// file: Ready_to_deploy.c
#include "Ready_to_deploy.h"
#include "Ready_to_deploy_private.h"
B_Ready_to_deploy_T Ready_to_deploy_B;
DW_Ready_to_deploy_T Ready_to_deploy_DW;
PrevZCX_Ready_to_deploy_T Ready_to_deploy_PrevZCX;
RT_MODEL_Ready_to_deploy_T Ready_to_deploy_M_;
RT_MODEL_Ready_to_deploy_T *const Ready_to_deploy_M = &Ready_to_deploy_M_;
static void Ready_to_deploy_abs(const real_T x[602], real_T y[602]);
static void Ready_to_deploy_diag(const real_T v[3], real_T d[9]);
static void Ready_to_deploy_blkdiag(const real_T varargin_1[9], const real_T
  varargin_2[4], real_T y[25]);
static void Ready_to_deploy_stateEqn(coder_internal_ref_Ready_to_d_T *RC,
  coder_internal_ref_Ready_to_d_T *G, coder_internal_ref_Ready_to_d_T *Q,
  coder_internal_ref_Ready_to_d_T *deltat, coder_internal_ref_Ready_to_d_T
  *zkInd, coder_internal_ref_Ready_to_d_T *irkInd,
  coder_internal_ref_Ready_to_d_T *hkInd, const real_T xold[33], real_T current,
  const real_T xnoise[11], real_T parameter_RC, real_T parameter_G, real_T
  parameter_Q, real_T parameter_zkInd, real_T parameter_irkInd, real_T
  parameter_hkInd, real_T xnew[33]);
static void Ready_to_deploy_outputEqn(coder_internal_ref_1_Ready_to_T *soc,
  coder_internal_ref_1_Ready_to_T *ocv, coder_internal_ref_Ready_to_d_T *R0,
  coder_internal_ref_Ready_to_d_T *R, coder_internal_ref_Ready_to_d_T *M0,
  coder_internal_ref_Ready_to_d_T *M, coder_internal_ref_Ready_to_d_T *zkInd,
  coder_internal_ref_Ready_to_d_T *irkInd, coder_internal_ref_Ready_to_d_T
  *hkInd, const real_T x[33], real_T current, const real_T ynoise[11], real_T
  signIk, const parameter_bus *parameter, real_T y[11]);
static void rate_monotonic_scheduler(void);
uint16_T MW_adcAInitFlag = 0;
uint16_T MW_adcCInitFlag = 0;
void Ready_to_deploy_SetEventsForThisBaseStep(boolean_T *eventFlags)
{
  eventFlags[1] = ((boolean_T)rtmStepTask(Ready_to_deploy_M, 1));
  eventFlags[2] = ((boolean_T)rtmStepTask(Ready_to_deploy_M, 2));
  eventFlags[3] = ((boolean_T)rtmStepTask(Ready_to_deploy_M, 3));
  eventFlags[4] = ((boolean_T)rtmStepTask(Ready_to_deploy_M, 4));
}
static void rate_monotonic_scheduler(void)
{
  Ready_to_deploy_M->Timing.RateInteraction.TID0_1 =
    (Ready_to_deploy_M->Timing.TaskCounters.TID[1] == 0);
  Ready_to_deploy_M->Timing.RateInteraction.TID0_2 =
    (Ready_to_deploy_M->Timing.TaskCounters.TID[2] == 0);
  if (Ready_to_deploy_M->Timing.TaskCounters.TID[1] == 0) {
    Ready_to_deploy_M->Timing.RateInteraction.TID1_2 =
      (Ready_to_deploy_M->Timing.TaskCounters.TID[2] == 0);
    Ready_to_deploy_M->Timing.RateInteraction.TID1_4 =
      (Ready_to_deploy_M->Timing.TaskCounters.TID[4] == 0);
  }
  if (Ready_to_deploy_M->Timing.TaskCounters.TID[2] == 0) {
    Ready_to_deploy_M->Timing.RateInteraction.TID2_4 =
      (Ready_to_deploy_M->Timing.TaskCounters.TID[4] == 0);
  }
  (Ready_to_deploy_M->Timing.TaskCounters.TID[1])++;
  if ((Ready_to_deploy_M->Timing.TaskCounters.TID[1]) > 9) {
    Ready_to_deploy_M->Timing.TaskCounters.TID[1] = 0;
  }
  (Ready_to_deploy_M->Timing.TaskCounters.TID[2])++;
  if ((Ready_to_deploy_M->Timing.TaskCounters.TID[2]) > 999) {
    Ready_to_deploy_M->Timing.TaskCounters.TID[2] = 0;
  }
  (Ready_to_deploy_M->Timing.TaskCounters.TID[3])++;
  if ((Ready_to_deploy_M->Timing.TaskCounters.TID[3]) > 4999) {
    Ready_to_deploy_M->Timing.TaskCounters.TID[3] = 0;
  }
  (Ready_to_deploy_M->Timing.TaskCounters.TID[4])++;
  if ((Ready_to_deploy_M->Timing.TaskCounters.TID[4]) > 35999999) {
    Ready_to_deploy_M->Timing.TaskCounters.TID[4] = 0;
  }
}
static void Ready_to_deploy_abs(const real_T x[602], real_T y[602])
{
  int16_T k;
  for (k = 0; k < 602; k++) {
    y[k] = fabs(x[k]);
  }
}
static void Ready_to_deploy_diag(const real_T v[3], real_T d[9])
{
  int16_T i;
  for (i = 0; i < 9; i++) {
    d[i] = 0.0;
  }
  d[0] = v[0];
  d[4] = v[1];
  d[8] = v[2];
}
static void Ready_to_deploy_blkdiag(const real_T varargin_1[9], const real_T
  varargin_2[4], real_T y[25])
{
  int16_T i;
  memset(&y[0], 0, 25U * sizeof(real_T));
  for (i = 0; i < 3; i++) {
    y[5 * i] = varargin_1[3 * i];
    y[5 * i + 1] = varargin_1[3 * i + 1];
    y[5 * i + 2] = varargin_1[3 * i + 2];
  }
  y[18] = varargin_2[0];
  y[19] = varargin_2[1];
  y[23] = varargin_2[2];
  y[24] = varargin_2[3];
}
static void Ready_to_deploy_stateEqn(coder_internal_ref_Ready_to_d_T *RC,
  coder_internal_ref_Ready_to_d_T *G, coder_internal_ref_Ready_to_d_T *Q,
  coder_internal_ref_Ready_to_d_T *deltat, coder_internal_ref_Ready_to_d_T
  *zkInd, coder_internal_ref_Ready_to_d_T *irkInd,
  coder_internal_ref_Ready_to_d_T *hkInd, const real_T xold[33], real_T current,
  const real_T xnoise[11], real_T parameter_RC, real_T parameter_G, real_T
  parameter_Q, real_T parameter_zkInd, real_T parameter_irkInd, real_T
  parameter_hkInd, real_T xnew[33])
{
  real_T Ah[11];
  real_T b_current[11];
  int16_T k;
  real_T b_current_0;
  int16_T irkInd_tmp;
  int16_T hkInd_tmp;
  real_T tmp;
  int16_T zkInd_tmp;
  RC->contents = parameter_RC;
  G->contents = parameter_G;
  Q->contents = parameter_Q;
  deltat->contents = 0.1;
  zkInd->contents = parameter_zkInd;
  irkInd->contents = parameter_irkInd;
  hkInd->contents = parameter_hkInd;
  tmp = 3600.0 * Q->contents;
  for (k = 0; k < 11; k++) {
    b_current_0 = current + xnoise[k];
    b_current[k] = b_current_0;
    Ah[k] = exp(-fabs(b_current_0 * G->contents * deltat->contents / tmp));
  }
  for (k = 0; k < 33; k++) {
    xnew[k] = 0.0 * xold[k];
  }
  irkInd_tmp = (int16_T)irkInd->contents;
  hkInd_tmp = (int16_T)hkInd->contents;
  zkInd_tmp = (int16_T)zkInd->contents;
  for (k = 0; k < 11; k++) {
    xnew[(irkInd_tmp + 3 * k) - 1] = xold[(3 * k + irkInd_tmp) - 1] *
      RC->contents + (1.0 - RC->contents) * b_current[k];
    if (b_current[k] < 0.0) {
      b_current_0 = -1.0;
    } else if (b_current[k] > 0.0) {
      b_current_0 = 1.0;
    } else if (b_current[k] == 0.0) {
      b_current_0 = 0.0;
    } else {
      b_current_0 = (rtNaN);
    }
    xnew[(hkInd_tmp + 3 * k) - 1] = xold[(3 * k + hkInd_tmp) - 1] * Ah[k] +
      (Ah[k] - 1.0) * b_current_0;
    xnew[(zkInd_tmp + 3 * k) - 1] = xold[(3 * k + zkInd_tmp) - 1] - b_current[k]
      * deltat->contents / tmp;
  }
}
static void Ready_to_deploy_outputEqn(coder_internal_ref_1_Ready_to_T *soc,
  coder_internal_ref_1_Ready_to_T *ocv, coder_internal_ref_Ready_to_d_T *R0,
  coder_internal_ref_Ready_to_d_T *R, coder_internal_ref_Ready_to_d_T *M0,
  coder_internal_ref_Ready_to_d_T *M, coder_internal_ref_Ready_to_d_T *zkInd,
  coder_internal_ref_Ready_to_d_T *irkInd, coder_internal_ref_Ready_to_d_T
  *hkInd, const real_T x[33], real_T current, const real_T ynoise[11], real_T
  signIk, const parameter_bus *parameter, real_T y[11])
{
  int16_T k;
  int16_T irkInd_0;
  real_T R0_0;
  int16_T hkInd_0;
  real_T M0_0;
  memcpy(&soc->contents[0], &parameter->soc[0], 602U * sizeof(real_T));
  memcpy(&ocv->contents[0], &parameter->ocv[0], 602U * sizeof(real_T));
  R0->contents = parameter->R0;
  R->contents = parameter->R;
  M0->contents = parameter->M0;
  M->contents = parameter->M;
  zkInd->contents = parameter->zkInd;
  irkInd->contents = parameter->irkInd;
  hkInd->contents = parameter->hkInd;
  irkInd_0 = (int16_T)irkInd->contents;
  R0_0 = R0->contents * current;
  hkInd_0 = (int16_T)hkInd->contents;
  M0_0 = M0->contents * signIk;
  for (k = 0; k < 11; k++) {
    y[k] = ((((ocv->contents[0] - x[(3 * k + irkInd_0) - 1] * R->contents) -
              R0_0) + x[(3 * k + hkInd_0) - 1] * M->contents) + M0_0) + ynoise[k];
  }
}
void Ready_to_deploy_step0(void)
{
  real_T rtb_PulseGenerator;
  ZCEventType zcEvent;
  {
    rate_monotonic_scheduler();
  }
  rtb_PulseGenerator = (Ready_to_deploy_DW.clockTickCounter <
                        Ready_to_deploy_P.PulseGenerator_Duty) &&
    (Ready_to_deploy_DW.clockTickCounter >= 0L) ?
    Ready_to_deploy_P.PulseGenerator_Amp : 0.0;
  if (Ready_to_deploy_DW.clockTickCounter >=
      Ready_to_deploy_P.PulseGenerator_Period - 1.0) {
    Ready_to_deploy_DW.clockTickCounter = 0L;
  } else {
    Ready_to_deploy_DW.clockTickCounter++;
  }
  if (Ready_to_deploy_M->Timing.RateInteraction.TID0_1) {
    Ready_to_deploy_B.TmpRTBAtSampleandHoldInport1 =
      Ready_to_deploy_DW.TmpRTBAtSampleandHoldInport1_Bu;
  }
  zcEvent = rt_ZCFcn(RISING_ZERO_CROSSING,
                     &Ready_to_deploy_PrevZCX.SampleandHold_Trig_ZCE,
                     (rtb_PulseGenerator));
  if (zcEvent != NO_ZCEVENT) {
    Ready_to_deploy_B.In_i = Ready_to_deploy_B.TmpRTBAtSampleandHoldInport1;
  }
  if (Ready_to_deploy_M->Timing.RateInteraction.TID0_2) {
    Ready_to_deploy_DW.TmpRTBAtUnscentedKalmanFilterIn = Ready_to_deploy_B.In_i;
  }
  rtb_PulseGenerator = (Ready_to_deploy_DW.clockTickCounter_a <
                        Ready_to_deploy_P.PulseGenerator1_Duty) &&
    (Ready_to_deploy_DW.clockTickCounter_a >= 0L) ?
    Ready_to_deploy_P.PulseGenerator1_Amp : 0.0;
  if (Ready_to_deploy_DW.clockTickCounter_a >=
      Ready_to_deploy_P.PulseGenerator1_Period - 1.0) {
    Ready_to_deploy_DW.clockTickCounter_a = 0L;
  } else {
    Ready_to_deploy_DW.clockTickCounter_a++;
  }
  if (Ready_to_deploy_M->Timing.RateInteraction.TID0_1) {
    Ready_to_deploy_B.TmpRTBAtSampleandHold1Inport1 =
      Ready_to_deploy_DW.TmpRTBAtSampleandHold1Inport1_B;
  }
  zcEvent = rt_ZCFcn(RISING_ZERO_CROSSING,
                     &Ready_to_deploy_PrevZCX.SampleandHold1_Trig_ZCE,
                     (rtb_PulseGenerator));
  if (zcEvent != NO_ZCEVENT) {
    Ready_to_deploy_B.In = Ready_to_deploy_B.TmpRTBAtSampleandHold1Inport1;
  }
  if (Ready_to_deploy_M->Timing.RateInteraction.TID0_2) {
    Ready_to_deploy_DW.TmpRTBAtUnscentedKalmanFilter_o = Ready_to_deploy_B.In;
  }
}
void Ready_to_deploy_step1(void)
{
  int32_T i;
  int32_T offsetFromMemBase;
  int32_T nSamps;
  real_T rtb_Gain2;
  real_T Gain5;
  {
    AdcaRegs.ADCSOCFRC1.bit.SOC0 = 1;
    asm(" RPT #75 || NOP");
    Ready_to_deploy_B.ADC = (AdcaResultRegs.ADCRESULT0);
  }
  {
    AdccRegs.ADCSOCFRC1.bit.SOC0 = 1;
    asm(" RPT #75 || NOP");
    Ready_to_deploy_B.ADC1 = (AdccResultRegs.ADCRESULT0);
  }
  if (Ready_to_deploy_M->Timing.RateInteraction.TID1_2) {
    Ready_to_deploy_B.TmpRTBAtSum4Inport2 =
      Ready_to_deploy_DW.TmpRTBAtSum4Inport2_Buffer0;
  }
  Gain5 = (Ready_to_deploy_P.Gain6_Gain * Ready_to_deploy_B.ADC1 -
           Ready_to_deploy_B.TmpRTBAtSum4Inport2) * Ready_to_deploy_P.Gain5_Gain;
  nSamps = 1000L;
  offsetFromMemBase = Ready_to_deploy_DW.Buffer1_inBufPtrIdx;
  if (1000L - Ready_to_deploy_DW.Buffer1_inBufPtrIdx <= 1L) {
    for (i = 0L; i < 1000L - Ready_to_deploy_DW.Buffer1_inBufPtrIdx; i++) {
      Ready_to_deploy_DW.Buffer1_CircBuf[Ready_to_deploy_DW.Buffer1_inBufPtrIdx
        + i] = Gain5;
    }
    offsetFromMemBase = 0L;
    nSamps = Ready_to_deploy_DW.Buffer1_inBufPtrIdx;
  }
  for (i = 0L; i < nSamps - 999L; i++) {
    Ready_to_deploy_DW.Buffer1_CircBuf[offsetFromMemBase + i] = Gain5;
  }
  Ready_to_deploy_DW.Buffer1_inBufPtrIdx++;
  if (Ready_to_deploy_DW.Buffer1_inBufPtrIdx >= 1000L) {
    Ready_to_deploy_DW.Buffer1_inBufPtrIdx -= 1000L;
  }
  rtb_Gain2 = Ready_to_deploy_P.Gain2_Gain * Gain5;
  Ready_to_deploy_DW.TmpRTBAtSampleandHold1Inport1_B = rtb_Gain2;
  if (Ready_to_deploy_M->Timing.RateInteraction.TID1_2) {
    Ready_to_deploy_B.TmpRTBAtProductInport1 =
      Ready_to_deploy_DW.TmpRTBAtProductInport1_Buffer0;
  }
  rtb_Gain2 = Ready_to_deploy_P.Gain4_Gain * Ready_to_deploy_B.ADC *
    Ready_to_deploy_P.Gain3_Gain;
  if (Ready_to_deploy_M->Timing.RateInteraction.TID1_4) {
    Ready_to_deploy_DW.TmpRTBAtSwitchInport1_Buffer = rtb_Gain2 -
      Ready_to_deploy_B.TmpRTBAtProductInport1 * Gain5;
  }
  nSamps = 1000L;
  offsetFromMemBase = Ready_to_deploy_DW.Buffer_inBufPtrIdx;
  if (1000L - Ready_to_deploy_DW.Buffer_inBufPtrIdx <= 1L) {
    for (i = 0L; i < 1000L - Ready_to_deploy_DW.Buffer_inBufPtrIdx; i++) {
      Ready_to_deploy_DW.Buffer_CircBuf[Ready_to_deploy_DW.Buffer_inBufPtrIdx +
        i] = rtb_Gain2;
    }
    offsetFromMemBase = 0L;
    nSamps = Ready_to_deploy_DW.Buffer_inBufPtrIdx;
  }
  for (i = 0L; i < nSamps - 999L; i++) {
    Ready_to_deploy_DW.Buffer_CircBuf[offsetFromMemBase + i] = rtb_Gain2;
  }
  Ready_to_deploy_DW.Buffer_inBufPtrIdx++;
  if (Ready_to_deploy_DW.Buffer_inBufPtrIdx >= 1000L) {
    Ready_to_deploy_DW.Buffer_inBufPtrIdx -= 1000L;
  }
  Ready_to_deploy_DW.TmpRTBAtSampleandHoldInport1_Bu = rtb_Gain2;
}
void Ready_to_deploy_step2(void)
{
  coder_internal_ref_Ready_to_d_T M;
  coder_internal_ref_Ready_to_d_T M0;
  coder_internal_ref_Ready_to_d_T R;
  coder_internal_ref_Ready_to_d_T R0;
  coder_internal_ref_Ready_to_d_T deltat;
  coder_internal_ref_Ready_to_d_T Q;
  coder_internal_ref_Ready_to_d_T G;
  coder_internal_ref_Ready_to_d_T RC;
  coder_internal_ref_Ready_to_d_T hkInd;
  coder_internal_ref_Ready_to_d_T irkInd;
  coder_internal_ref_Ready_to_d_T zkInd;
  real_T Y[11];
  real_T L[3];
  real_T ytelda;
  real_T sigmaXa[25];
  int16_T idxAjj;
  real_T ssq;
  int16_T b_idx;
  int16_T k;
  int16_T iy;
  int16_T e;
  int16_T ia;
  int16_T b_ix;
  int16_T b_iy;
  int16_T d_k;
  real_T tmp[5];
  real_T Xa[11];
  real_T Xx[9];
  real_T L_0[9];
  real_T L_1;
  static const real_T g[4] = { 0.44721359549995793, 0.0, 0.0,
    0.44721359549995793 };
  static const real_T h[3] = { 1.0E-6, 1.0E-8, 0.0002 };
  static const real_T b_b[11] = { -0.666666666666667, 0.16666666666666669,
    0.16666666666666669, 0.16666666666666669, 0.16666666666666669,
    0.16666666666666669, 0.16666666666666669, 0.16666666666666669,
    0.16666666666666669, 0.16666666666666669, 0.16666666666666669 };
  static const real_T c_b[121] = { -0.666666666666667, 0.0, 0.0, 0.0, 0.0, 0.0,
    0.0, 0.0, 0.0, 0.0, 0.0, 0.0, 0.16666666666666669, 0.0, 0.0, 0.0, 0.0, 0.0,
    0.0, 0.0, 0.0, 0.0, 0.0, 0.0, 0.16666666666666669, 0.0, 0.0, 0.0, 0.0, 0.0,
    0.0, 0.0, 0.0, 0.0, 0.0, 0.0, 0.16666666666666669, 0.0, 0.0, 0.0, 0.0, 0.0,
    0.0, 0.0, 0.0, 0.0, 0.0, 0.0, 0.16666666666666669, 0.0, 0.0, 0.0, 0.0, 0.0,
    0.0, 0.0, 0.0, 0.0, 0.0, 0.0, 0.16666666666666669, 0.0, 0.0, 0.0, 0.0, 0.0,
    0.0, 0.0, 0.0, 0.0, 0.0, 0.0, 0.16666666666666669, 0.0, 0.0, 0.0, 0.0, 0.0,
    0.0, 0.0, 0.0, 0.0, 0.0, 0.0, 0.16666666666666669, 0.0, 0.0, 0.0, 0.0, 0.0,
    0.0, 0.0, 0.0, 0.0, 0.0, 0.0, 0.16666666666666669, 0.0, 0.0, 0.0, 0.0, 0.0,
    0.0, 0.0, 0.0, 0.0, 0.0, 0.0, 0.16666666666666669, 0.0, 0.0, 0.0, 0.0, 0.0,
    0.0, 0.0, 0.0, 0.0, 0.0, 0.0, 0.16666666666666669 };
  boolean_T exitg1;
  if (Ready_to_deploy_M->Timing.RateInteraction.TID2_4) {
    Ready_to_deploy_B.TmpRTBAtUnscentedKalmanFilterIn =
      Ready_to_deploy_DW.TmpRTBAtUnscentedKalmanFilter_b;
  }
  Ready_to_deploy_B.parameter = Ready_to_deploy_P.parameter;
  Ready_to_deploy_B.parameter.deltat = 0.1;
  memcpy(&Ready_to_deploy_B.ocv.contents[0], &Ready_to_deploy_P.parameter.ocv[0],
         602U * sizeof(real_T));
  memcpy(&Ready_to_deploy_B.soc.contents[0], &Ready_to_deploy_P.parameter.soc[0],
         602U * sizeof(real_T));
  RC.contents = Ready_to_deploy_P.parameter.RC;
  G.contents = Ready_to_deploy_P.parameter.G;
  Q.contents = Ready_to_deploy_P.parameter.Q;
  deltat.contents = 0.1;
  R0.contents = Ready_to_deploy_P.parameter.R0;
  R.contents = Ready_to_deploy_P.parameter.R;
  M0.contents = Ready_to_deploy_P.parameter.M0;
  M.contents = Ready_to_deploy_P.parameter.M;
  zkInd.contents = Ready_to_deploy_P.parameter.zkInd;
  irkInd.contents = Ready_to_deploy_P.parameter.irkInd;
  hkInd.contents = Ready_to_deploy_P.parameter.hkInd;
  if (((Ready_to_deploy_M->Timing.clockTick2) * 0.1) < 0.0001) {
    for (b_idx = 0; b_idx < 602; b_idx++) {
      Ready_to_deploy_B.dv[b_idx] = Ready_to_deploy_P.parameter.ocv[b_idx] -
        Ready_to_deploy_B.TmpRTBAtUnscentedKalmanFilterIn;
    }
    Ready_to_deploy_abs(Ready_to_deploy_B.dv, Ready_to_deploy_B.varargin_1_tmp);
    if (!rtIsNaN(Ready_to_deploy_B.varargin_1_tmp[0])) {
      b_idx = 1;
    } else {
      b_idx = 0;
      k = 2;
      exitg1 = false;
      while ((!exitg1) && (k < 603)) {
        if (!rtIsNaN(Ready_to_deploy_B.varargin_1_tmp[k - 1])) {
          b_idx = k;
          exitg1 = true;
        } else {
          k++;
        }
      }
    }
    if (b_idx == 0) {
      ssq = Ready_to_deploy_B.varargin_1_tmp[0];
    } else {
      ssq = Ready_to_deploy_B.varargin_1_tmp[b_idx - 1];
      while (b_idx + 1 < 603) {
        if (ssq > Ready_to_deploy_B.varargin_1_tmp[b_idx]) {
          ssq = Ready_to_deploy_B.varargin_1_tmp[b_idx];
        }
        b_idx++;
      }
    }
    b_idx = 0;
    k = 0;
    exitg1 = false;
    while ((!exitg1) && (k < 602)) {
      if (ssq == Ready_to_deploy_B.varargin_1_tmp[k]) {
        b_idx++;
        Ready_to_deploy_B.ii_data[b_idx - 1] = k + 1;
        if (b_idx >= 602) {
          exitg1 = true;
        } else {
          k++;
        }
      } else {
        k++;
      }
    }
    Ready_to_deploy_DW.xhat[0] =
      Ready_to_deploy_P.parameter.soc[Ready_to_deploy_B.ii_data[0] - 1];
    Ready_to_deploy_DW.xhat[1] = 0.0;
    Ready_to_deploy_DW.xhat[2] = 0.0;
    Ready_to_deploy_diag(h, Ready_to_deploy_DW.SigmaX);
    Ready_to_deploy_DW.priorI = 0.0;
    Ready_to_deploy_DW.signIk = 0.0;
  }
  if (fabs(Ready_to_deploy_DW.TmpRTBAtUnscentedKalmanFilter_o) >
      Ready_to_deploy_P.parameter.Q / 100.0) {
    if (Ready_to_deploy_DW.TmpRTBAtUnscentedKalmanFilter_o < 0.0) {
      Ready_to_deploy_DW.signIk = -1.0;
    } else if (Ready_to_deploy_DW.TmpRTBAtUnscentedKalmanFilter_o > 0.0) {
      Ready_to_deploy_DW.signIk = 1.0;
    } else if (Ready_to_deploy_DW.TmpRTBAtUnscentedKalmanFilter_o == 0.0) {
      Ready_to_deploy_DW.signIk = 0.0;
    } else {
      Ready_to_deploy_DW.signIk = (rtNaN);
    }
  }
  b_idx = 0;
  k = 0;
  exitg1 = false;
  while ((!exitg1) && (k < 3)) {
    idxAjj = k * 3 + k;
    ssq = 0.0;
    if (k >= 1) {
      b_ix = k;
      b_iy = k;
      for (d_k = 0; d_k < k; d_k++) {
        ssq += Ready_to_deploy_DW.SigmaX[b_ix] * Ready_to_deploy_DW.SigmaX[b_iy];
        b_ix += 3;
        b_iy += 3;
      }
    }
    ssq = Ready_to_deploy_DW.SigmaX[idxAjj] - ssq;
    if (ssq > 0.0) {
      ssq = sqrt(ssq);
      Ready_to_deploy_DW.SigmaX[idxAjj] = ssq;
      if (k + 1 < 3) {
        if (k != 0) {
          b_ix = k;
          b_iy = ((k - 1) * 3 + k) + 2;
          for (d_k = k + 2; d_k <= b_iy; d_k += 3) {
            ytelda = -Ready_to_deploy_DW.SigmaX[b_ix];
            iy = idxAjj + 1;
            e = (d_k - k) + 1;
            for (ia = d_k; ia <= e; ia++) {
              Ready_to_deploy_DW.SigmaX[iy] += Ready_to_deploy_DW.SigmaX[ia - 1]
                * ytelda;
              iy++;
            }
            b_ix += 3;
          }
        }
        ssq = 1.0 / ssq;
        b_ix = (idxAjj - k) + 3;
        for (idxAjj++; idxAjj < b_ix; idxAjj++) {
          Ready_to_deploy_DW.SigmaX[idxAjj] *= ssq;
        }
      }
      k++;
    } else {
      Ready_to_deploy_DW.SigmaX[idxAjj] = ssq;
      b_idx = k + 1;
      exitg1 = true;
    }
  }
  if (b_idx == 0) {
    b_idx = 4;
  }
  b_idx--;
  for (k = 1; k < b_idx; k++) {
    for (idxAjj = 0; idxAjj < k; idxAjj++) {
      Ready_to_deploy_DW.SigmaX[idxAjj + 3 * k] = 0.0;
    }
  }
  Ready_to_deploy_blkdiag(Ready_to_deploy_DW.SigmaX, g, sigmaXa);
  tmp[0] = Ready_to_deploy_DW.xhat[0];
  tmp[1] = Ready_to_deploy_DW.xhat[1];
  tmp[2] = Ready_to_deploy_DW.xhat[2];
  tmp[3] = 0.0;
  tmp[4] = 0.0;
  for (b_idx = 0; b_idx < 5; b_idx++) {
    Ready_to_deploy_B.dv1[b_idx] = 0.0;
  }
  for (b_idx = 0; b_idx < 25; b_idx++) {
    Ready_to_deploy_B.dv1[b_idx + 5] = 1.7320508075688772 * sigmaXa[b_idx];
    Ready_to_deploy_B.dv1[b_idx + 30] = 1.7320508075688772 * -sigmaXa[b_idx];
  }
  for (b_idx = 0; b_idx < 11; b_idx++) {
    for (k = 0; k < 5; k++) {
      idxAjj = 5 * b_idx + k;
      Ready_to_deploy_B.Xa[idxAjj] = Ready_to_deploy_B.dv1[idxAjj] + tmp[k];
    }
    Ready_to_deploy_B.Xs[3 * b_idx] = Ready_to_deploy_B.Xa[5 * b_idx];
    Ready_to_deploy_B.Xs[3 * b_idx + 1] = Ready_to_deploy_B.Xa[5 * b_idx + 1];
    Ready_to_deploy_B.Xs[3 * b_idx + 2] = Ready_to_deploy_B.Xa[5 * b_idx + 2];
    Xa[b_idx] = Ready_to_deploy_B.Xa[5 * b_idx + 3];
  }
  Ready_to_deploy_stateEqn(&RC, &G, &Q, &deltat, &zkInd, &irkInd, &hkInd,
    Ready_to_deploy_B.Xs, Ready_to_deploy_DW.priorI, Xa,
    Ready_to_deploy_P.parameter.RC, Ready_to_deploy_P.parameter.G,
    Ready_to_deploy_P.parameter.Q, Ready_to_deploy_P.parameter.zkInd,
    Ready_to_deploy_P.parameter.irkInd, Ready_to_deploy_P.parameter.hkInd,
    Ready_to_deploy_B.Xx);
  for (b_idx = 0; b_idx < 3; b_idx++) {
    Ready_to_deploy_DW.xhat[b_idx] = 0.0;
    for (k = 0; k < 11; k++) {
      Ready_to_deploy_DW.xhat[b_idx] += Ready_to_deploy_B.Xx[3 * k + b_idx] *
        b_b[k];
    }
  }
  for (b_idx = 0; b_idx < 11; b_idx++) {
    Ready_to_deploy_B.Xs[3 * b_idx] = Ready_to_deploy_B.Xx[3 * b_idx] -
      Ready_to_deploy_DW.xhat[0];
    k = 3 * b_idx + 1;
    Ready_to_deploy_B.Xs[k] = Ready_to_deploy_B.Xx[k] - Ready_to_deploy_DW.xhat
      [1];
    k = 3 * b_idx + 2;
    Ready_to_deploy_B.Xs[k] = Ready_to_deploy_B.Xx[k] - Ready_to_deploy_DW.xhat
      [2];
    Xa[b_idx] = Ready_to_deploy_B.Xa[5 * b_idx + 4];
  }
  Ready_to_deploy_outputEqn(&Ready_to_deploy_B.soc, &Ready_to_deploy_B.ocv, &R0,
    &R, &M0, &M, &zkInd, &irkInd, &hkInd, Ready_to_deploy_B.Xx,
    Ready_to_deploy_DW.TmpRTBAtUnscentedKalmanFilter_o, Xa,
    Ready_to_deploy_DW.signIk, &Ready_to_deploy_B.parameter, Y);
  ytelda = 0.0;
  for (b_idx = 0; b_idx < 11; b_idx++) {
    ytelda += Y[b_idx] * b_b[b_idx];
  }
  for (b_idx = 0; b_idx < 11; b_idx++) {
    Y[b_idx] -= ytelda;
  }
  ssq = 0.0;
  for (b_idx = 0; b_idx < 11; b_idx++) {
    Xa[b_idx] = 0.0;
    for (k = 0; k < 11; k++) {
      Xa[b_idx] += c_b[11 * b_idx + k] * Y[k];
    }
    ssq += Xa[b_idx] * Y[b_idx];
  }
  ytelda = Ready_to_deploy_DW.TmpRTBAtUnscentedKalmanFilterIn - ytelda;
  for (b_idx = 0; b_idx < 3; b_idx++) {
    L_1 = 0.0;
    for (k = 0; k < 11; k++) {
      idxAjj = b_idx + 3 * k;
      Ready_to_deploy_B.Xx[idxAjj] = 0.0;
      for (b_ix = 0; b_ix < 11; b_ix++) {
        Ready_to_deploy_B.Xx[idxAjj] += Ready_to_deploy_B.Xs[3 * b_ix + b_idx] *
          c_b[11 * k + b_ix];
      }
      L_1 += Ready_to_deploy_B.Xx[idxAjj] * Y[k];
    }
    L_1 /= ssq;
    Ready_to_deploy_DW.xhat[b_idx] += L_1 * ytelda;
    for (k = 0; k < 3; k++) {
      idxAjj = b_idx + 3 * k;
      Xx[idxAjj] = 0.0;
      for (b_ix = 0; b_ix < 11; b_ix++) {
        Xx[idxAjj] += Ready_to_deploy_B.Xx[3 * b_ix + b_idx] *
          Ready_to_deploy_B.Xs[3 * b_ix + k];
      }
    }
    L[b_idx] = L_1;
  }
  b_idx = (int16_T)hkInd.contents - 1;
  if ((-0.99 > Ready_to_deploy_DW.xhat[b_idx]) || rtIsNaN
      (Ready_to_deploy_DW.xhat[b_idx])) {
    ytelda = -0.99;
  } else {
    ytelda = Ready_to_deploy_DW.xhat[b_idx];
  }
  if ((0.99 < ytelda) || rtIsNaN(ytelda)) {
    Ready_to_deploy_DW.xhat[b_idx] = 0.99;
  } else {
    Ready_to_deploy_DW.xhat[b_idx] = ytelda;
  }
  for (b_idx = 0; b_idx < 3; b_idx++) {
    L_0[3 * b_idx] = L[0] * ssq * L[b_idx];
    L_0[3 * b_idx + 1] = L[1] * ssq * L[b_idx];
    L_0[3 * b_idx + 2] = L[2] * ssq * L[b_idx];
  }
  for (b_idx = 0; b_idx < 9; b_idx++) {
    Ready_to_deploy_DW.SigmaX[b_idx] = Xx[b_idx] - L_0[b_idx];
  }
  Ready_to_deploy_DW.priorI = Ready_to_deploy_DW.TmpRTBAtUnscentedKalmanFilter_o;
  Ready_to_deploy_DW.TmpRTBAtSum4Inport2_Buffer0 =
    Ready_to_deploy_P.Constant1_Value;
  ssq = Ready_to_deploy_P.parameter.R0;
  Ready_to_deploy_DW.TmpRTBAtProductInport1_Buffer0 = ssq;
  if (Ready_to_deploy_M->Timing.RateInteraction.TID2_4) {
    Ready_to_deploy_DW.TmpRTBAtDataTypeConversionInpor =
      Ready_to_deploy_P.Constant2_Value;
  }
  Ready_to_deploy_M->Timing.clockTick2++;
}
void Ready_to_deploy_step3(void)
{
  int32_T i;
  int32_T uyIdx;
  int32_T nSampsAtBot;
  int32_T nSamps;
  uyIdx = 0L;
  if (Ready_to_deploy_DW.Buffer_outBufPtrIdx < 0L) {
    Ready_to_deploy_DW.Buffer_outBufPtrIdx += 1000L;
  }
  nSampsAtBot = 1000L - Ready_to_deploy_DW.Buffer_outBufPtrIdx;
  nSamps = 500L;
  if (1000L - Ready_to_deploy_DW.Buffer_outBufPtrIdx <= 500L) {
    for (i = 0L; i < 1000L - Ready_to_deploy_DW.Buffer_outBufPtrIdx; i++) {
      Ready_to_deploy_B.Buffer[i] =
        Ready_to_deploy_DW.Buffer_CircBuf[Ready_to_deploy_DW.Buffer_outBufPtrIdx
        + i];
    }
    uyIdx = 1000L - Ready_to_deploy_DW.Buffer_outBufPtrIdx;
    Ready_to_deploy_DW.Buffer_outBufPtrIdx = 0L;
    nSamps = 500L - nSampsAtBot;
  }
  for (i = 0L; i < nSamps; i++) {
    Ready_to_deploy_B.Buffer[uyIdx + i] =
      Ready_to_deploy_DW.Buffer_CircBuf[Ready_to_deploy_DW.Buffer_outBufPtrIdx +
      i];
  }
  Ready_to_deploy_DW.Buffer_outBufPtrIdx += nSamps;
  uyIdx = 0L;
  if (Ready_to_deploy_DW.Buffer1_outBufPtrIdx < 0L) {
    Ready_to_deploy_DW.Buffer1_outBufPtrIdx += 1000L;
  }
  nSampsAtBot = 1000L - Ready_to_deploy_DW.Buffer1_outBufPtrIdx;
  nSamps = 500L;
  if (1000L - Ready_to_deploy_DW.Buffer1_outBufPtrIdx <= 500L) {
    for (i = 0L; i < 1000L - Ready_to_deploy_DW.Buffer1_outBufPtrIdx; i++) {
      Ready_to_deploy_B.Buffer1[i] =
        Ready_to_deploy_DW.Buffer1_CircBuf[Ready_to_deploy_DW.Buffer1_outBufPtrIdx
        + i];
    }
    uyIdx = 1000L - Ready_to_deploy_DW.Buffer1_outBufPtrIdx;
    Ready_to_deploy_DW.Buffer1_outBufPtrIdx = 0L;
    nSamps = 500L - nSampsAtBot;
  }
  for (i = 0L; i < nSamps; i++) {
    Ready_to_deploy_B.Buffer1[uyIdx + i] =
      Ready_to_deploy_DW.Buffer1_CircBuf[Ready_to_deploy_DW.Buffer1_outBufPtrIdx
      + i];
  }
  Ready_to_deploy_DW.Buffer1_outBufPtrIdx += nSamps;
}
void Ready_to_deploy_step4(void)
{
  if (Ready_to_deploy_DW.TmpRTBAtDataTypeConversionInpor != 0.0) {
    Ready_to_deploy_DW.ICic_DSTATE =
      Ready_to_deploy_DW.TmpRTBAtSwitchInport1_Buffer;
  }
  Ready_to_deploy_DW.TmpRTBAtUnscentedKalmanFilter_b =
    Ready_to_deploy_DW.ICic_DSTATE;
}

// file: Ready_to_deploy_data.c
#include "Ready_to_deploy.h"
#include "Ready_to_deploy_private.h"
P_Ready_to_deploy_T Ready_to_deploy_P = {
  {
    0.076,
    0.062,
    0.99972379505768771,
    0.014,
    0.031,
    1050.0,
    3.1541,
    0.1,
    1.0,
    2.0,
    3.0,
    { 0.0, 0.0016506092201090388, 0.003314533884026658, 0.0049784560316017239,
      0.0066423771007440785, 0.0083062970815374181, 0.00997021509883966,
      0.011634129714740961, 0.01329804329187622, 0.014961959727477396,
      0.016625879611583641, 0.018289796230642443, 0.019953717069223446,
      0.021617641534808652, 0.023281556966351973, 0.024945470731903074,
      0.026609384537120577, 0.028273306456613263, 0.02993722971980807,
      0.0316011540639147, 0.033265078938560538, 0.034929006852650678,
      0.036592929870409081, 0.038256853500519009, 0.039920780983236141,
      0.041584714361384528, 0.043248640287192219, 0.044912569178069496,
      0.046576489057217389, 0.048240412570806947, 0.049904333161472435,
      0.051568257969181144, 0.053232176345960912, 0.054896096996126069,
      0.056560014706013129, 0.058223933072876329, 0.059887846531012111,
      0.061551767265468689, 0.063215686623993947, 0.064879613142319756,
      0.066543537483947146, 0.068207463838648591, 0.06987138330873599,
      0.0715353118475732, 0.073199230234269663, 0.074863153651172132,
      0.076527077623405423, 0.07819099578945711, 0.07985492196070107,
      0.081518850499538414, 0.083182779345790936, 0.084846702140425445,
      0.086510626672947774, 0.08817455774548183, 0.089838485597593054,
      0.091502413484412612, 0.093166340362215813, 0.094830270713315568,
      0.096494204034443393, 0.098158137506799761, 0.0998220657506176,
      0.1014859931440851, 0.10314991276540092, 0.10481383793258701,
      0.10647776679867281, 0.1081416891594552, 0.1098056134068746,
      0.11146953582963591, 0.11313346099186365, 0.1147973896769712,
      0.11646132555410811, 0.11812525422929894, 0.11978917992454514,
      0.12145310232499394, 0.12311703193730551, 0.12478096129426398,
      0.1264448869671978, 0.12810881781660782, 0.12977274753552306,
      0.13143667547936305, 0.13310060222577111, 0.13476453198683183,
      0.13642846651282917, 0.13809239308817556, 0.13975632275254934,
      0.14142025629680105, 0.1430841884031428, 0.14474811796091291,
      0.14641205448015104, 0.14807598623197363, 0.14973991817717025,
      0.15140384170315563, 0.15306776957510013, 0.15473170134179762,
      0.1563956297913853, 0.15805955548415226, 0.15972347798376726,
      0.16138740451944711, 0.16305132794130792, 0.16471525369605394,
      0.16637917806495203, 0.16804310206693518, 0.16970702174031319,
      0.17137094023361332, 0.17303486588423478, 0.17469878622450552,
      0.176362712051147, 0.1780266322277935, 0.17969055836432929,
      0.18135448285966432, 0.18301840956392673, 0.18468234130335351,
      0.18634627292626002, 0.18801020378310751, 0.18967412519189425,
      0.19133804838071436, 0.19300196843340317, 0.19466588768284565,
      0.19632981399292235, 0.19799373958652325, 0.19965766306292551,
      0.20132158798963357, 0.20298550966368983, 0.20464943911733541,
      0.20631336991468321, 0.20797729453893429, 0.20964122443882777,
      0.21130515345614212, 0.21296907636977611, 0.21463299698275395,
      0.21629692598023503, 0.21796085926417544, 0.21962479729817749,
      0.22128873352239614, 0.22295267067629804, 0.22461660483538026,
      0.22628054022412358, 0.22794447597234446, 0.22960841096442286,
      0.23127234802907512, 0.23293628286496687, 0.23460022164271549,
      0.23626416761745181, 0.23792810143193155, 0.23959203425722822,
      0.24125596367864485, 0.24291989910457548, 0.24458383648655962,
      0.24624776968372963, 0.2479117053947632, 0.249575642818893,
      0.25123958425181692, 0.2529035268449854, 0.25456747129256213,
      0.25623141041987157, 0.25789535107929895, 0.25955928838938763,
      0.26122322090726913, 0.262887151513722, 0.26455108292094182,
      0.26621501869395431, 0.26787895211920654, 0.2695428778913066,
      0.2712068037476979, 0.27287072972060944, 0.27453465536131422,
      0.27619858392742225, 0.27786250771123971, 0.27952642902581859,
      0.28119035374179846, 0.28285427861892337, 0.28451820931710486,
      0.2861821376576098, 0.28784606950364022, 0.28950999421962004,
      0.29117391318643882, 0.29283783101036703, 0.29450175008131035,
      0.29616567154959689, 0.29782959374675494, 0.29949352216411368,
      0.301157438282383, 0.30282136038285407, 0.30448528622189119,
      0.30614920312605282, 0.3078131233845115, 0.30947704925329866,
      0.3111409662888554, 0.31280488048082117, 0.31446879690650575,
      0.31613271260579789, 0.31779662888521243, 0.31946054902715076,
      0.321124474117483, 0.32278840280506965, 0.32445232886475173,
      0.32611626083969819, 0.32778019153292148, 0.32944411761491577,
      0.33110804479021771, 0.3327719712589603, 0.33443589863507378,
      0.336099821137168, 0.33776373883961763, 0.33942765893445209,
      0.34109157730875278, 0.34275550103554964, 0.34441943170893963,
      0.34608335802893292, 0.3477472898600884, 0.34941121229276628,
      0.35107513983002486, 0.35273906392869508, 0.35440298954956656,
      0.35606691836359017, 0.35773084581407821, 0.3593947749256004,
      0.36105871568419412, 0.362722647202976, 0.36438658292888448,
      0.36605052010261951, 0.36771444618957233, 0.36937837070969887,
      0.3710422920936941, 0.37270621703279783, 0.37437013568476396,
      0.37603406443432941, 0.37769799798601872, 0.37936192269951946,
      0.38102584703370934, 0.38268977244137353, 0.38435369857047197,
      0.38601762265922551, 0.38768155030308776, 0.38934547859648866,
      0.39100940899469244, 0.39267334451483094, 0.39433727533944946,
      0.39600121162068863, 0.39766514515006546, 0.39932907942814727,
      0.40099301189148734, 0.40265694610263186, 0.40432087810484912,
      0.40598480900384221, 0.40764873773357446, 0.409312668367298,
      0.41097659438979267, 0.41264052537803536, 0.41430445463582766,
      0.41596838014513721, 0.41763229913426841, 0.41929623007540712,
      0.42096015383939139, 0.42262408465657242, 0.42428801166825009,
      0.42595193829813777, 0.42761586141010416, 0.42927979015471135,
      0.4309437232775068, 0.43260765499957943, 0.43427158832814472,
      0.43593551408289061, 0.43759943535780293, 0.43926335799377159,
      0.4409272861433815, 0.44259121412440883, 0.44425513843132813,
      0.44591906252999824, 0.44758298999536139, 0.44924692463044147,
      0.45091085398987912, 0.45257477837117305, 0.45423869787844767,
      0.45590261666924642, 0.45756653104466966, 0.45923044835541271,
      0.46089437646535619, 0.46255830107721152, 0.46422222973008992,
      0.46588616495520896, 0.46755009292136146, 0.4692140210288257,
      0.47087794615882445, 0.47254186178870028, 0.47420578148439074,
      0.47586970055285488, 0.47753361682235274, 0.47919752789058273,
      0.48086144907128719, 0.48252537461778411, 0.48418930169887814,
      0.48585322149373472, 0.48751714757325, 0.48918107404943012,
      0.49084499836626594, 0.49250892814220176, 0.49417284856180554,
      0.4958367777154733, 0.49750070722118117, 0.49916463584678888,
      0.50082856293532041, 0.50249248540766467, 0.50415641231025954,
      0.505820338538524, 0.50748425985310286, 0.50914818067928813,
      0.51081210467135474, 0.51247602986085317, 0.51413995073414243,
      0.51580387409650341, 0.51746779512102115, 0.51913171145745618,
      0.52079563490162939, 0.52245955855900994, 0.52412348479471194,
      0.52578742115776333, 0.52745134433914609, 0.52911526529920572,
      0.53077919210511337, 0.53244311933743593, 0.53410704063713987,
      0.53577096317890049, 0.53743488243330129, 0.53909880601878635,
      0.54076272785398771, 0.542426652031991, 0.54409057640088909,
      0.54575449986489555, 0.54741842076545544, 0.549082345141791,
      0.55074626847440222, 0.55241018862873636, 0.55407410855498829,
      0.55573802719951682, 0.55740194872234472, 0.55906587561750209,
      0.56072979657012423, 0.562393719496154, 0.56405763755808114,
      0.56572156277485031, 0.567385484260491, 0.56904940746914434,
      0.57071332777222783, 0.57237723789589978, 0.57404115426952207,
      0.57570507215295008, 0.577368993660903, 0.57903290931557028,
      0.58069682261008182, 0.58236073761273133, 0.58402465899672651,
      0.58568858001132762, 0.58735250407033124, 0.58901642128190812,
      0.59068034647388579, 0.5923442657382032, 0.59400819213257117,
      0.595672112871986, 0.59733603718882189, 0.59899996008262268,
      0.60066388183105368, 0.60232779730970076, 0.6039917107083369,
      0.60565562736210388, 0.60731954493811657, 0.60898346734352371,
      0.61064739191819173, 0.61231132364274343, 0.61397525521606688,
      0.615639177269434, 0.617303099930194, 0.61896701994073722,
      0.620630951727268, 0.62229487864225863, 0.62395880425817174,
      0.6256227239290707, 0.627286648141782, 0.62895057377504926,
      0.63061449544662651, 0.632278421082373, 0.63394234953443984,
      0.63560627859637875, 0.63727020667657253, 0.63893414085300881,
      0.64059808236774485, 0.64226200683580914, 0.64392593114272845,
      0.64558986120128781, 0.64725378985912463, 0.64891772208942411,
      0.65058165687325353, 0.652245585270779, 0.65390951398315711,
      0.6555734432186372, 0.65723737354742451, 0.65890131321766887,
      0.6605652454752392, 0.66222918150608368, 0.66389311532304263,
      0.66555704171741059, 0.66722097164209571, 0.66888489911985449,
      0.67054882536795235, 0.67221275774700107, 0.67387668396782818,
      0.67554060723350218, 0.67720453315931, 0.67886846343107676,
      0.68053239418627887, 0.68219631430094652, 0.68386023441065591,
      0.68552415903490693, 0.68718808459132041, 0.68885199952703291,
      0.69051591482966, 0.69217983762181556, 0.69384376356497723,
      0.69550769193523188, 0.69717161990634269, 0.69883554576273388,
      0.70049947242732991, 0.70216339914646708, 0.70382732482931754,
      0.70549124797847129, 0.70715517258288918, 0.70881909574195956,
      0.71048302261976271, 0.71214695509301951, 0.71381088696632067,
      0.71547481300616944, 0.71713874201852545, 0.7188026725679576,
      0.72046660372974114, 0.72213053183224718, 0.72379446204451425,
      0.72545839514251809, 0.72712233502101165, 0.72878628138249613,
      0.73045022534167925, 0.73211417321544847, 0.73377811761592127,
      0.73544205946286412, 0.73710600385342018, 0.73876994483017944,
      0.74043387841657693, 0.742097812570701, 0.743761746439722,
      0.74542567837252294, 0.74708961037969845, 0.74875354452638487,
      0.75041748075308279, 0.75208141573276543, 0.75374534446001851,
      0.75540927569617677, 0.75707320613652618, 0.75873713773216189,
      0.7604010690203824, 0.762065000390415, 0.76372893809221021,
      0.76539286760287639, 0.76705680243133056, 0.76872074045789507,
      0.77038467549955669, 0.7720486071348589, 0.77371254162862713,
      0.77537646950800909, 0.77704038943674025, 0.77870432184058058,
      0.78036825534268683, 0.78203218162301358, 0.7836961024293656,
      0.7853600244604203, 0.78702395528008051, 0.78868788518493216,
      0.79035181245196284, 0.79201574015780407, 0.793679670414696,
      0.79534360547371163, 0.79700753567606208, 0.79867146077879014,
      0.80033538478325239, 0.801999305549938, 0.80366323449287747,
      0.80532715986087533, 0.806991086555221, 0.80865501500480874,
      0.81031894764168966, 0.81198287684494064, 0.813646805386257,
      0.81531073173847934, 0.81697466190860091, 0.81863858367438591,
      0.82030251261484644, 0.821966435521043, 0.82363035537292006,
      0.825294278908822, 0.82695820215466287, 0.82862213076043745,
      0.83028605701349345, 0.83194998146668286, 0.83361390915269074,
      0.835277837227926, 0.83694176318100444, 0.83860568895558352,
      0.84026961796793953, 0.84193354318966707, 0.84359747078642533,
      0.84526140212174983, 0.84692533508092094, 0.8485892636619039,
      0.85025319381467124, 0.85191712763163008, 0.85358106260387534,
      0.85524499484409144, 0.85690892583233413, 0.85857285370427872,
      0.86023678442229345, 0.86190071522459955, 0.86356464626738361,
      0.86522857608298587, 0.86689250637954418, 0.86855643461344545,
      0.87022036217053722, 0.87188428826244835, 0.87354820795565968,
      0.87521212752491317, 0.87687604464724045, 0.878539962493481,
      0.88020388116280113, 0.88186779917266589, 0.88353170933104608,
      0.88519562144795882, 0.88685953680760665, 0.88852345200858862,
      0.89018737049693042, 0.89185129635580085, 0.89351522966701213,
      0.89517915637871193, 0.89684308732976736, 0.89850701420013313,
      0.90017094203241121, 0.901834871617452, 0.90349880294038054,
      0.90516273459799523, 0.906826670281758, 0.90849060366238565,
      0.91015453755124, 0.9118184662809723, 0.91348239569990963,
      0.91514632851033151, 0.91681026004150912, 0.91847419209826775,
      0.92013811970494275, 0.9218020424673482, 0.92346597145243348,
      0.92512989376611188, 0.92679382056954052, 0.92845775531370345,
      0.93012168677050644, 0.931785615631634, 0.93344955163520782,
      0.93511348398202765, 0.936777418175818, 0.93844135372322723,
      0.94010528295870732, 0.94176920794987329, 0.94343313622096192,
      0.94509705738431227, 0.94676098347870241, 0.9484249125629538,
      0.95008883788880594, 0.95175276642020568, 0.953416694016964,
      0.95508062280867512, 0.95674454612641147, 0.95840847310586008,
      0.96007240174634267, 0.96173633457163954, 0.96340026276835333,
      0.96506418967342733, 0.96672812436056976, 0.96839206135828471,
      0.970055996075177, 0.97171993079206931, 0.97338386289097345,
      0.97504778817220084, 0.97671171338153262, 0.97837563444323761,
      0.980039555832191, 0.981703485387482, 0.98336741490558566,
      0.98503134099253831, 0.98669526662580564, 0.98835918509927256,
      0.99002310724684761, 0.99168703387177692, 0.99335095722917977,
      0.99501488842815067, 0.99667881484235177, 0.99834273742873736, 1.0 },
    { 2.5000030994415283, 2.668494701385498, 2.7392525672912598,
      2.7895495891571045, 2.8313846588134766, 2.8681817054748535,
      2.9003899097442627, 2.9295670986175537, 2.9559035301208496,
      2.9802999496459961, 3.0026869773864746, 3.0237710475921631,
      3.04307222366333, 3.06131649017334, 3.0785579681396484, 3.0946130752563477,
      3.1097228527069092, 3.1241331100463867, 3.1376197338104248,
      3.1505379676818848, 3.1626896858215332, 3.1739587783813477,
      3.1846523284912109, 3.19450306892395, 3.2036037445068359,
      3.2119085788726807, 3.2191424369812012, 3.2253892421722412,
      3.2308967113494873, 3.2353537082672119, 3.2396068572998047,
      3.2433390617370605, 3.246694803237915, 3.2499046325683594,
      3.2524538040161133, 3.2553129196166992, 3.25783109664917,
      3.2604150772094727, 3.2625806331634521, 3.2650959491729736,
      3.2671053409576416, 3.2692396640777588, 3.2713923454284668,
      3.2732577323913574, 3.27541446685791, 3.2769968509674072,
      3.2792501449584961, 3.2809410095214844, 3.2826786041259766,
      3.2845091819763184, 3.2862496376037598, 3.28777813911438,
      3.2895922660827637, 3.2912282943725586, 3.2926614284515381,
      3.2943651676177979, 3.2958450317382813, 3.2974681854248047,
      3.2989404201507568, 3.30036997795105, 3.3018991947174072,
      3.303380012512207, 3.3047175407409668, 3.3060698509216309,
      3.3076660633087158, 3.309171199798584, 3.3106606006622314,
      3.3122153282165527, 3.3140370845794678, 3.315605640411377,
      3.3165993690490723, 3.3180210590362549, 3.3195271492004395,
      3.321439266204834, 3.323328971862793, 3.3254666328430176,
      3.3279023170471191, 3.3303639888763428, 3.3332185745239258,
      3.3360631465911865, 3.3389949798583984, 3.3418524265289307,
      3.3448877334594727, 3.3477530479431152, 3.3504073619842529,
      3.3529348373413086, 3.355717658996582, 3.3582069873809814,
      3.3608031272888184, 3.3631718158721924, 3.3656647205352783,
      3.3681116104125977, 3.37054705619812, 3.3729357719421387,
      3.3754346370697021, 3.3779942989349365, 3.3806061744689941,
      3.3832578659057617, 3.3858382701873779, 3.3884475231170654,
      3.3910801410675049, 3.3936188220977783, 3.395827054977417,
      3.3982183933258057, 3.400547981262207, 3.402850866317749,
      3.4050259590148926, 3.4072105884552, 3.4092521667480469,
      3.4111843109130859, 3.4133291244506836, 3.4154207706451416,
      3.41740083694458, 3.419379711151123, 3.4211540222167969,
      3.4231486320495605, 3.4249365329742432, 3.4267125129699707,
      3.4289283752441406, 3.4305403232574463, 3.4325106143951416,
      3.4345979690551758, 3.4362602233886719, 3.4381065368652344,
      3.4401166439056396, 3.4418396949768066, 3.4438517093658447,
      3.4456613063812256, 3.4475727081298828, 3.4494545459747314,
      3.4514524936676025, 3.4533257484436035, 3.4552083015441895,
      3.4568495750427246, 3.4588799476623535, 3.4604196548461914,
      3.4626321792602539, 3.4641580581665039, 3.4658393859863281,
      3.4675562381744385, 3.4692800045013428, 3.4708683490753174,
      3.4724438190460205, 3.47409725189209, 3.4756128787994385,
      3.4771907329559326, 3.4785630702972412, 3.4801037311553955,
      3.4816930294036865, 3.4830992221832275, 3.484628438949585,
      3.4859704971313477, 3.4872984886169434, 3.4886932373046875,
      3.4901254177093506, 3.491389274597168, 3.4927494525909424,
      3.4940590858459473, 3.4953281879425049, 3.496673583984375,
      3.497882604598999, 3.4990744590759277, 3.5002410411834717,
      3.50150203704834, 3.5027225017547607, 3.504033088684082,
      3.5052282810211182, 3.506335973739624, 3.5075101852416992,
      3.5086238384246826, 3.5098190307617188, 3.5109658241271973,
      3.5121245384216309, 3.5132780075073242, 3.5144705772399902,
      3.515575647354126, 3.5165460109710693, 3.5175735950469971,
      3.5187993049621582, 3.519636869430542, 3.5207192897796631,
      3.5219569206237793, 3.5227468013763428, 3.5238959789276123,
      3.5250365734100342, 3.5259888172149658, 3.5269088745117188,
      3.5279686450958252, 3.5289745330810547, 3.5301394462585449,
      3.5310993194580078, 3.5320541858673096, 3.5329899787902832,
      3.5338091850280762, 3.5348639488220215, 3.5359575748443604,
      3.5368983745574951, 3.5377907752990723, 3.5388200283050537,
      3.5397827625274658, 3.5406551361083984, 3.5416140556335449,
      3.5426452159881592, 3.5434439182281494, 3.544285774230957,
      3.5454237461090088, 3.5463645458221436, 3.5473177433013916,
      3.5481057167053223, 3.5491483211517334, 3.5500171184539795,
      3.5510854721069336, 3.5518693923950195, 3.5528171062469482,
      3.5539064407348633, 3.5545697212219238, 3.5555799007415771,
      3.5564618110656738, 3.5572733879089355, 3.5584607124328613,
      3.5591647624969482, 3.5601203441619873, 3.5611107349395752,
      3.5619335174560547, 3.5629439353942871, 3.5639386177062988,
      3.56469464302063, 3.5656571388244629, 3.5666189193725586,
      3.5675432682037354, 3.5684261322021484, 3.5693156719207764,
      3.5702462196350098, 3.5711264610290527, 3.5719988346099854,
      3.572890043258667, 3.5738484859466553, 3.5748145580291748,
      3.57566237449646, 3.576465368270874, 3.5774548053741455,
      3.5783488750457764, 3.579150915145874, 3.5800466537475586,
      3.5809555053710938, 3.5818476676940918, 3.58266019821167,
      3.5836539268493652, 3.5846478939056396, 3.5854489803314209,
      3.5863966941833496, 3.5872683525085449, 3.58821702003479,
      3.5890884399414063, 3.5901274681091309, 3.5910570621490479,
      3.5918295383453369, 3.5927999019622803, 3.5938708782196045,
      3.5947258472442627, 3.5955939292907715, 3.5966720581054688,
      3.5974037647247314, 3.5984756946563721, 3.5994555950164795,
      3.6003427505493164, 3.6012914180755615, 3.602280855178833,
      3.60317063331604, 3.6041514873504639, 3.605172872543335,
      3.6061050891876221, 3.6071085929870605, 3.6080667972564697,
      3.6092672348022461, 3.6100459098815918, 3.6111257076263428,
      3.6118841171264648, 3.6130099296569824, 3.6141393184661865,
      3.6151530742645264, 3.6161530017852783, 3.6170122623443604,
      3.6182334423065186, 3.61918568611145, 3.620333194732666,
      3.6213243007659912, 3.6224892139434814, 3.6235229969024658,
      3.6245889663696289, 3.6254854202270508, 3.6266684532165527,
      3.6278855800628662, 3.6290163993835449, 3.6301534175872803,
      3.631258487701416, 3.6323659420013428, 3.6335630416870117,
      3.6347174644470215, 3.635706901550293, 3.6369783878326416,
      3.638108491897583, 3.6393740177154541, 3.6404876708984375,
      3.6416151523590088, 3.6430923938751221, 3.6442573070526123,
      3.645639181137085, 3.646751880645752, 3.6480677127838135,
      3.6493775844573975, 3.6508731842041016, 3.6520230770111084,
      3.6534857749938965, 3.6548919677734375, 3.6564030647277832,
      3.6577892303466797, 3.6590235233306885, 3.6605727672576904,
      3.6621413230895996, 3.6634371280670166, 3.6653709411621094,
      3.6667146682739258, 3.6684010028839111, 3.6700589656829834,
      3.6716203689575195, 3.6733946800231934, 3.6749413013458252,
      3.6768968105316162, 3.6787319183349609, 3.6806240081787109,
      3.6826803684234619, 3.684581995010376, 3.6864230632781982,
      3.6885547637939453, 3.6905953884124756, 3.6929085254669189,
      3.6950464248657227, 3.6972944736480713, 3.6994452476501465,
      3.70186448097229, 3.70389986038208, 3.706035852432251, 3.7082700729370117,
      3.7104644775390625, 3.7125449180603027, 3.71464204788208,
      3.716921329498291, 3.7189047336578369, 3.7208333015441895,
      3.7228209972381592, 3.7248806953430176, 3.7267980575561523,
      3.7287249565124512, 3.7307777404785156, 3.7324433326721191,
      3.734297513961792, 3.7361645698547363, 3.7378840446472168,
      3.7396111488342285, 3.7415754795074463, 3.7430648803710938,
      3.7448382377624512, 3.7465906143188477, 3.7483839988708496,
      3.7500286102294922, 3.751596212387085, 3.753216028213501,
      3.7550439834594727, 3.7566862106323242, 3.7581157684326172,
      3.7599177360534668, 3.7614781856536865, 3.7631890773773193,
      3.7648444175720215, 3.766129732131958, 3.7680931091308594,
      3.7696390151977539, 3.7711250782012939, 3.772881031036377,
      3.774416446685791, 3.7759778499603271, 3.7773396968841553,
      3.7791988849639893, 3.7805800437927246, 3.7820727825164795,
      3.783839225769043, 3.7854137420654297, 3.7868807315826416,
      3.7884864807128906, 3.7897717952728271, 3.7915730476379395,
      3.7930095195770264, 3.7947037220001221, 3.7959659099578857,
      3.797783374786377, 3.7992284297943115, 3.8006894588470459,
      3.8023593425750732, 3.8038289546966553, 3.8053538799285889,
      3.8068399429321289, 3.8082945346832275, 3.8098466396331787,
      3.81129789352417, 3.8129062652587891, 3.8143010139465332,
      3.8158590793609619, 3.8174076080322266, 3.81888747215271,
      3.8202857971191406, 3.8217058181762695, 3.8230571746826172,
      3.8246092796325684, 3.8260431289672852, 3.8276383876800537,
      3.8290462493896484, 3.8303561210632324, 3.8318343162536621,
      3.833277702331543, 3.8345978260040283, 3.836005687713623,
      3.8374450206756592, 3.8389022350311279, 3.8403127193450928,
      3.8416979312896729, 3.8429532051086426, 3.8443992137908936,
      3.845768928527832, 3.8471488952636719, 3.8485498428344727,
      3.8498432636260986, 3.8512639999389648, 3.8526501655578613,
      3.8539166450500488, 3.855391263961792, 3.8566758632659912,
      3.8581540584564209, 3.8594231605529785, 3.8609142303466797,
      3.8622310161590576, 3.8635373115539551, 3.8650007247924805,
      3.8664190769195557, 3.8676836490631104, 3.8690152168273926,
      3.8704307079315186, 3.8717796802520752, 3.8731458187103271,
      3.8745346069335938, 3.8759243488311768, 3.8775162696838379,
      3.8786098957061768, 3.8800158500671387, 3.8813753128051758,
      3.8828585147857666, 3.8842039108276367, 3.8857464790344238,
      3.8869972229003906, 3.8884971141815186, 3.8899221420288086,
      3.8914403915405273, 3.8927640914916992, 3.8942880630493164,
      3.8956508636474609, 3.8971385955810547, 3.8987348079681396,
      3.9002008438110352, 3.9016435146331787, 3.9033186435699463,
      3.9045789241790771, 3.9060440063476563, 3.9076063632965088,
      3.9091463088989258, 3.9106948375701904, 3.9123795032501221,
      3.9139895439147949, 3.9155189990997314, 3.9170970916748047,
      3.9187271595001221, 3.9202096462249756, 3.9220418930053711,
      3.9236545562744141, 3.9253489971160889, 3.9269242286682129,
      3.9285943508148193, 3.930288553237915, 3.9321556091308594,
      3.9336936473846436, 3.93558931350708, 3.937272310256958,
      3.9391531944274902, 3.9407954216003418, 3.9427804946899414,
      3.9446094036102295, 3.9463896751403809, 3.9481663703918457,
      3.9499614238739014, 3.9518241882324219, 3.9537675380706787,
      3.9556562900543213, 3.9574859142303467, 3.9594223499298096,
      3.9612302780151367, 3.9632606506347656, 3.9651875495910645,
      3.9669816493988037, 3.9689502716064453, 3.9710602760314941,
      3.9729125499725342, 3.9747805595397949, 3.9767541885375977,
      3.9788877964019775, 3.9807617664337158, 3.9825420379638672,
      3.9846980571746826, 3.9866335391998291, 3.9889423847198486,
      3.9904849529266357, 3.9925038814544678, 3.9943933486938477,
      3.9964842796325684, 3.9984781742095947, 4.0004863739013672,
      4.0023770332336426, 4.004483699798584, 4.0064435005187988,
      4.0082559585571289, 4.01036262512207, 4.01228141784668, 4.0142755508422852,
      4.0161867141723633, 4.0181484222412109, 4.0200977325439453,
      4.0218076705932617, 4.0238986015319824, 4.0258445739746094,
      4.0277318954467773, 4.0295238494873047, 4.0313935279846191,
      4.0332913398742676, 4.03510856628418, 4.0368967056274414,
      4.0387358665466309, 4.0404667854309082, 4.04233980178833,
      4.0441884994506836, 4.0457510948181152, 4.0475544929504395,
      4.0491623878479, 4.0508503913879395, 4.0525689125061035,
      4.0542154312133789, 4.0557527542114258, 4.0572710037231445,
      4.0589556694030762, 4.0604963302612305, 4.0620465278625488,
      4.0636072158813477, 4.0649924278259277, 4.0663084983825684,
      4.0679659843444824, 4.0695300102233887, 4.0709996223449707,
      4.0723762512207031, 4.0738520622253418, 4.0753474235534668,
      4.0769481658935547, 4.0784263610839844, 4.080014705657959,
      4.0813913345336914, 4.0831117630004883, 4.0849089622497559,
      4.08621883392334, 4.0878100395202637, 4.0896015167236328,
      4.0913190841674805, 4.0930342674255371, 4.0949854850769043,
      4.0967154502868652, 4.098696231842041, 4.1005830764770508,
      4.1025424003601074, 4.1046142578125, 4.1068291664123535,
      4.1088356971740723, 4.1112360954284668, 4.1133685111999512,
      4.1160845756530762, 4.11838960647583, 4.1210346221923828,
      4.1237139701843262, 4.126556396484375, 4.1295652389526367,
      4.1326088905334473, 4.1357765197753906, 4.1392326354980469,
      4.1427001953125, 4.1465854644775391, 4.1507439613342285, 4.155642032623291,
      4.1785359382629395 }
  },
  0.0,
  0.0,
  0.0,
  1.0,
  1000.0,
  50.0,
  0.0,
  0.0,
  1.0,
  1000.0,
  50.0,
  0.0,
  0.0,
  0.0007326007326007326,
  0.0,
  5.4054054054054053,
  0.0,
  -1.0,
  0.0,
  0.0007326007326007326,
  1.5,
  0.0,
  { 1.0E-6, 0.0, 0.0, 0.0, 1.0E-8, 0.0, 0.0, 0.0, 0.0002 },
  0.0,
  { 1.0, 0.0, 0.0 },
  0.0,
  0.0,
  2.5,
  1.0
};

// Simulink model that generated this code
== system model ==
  MemoryCopy#1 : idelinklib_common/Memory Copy  <- 1: Buffer1
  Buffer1 : Buffer  N=500  <- 1: Gain5
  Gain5 : Gain  Gain=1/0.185  <- 1: Sum#1
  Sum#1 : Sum  Inputs=+-  <- 1: Gain6, 2: Constant1
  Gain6 : Gain  Gain=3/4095  <- 1: ADC1
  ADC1 : c2802xlib/ADC
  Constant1 : Constant  Value=2.5
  MemoryCopy#2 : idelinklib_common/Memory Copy  <- 1: Buffer
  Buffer : Buffer  N=500  <- 1: Gain3
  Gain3 : Gain  Gain=1.5  <- 1: Gain4
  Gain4 : Gain  Gain=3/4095  <- 1: ADC
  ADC : c2802xlib/ADC
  MATLABFunction#1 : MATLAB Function  <- 1: SampleandHold, 2: SampleandHold1, 3: DigitalClock#1, 4: SampleandHold#1, 5: Constant#1, 6: UnitDelay#1, 7: UnitDelay#2, 8: UnitDelay#3, 9: UnitDelay#4
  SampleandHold : dspsigops/Sample and Hold  <- 1: Gain3, Trigger: PulseGenerator
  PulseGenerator : DiscretePulseGenerator  Period=1e-1  PulseWidth=5
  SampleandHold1 : dspsigops/Sample and Hold  <- 1: Gain2, Trigger: PulseGenerator1
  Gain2 : Gain  Gain=-1  <- 1: Gain5
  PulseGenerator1 : DiscretePulseGenerator  Period=1e-1  PulseWidth=5
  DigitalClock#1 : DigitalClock
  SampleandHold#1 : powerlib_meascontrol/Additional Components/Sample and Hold  <- 1: Sum#2, 2: Constant2
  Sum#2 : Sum  Inputs=-+  <- 1: Product#1, 2: Gain3
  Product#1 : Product  <- 1: R0, 2: Gain5
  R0 : Constant  Value=parameter.R0
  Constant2 : Constant
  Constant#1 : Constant  Value=parameter
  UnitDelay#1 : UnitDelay  InitialCondition=[1;0;0]  <- 1: MATLABFunction#1/3
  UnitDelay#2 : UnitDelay  InitialCondition=diag([1e-6 1e-8 2e-4])  <- 1: MATLABFunction#1/4
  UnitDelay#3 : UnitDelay  <- 1: MATLABFunction#1/5
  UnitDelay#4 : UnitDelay  <- 1: MATLABFunction#1/6
== matlab function MATLABFunction#1 ==
function [zk,zkbnd,xhat,SigmaX,priorI,signIk] = iterSPKF(vk,ik,t,v0,parameter,xhat,SigmaX,priorI,signIk)
parameter.deltat=1e-1;
SigmaX0 = diag([1e-6 1e-8 2e-4]);
SigmaV = 2e-1;
SigmaW = 2e-1;
Snoise = chol(blkdiag(SigmaW,SigmaV),'lower');
irk0 = 0;
hk0 = 0;
zkInd = 1;
irkInd = 2;
hkInd = 3;
ocv=parameter.ocv;
soc=parameter.soc;
Nx = 3;
Nw = 1;
Nv = 1;
Na = Nx+Nw+Nv;
h = sqrt(3);
alpha1 = (h*h-Na)/(h*h);
alpha2 = 1/(2*h*h);
alpham = [alpha1; alpha2*ones(2*Na,1)];
alphac = alpham;
RC      = parameter.RC;
G       = parameter.G;
Q       = parameter.Q;
deltat  = parameter.deltat;
R0      = parameter.R0;
R       = parameter.R;
M0      = parameter.M0;
M       = parameter.M;
zkInd   = parameter.zkInd;
irkInd  = parameter.irkInd;
hkInd   = parameter.hkInd;

eta     = 1;
if ik<0 
ik=ik*eta;
end

if t<1e-4
j1=find(min(abs(ocv-v0))==abs(ocv-v0));
j=j1(1,:);
SOC0 = soc(j);
xhat = [SOC0;irk0;hk0];
SigmaX = SigmaX0;
priorI = 0;
signIk = 0;
end

I       =  priorI;
if abs(ik)>Q/100
signIk = sign(ik);
end
xhata = [xhat; zeros([Nw+Nv 1])];
sigmaXa = chol(SigmaX,'lower');
sigmaXa= blkdiag(sigmaXa,Snoise);
Xa = xhata(:,ones([1 2*Na+1])) + h*[zeros([Na 1]),sigmaXa,-sigmaXa];
Xx = stateEqn(Xa(1:Nx,:),I,Xa(Nx+1:Nx+Nw,:),parameter);
xhat = Xx*alpham;
Xs = Xx - xhat(:,ones([1 2*Na+1]));
SigmaX = Xs*diag(alphac)*Xs';
I = ik;
yk = vk;
Y = outputEqn(Xx,I,Xa(5,:),signIk,parameter);
yhat = Y*alpham;
Ys = Y - yhat(:,ones([1 2*Na+1]));
SigmaXY = Xs*diag(alphac)*Ys';
SigmaY = Ys*diag(alphac)*Ys';
L = SigmaXY/SigmaY;
ytelda = yk - yhat;
xhat = xhat + L*ytelda;
xhat(hkInd) = min(0.99,max(-0.99,xhat(hkInd)));
SigmaX = SigmaX - L*SigmaY*L';
priorI = ik;
zk = xhat(zkInd);
zkbnd = 3*sqrt(SigmaX(zkInd,zkInd));
function xnew = stateEqn(xold,current,xnoise,parameter)
current = current + xnoise;
RC      = parameter.RC;
G       = parameter.G;
Q       = parameter.Q;
deltat  = parameter.deltat;
zkInd   = parameter.zkInd;
irkInd  = parameter.irkInd;
hkInd   = parameter.hkInd;
Ah = exp(-abs(current*G*deltat/(3600*Q)));
xnew = 0*xold;
xnew(irkInd,:) = RC*xold(irkInd,:) + (1-RC)*current;
xnew(hkInd,:) = Ah.*xold(hkInd,:) + (Ah-1).*sign(current);
xnew(zkInd,:) = xold(zkInd,:) - current*deltat/(3600*Q);
end
function y = outputEqn(x,current,ynoise,signIk,parameter)
soc     = parameter.soc;
ocv     = parameter.ocv;
R0      = parameter.R0;
R       = parameter.R;
M0      = parameter.M0;
M       = parameter.M;
zkInd   = parameter.zkInd;
irkInd  = parameter.irkInd;
hkInd   = parameter.hkInd;
i = zeros(11,1);
for k=1:11
i2=find(min(abs(soc-x(zkInd,k)*ones(length(soc),1)))==abs(soc-x(zkInd,k)*ones(length(soc),1)));
i2(1)=min(1,max(length(soc),i2(1)));
i(k,1)=i2(1,1);
end
y = ocv(i)' - R * x(irkInd,:) - R0 * current + M * x(hkInd,:) + M0 * signIk + ynoise;
end
end
